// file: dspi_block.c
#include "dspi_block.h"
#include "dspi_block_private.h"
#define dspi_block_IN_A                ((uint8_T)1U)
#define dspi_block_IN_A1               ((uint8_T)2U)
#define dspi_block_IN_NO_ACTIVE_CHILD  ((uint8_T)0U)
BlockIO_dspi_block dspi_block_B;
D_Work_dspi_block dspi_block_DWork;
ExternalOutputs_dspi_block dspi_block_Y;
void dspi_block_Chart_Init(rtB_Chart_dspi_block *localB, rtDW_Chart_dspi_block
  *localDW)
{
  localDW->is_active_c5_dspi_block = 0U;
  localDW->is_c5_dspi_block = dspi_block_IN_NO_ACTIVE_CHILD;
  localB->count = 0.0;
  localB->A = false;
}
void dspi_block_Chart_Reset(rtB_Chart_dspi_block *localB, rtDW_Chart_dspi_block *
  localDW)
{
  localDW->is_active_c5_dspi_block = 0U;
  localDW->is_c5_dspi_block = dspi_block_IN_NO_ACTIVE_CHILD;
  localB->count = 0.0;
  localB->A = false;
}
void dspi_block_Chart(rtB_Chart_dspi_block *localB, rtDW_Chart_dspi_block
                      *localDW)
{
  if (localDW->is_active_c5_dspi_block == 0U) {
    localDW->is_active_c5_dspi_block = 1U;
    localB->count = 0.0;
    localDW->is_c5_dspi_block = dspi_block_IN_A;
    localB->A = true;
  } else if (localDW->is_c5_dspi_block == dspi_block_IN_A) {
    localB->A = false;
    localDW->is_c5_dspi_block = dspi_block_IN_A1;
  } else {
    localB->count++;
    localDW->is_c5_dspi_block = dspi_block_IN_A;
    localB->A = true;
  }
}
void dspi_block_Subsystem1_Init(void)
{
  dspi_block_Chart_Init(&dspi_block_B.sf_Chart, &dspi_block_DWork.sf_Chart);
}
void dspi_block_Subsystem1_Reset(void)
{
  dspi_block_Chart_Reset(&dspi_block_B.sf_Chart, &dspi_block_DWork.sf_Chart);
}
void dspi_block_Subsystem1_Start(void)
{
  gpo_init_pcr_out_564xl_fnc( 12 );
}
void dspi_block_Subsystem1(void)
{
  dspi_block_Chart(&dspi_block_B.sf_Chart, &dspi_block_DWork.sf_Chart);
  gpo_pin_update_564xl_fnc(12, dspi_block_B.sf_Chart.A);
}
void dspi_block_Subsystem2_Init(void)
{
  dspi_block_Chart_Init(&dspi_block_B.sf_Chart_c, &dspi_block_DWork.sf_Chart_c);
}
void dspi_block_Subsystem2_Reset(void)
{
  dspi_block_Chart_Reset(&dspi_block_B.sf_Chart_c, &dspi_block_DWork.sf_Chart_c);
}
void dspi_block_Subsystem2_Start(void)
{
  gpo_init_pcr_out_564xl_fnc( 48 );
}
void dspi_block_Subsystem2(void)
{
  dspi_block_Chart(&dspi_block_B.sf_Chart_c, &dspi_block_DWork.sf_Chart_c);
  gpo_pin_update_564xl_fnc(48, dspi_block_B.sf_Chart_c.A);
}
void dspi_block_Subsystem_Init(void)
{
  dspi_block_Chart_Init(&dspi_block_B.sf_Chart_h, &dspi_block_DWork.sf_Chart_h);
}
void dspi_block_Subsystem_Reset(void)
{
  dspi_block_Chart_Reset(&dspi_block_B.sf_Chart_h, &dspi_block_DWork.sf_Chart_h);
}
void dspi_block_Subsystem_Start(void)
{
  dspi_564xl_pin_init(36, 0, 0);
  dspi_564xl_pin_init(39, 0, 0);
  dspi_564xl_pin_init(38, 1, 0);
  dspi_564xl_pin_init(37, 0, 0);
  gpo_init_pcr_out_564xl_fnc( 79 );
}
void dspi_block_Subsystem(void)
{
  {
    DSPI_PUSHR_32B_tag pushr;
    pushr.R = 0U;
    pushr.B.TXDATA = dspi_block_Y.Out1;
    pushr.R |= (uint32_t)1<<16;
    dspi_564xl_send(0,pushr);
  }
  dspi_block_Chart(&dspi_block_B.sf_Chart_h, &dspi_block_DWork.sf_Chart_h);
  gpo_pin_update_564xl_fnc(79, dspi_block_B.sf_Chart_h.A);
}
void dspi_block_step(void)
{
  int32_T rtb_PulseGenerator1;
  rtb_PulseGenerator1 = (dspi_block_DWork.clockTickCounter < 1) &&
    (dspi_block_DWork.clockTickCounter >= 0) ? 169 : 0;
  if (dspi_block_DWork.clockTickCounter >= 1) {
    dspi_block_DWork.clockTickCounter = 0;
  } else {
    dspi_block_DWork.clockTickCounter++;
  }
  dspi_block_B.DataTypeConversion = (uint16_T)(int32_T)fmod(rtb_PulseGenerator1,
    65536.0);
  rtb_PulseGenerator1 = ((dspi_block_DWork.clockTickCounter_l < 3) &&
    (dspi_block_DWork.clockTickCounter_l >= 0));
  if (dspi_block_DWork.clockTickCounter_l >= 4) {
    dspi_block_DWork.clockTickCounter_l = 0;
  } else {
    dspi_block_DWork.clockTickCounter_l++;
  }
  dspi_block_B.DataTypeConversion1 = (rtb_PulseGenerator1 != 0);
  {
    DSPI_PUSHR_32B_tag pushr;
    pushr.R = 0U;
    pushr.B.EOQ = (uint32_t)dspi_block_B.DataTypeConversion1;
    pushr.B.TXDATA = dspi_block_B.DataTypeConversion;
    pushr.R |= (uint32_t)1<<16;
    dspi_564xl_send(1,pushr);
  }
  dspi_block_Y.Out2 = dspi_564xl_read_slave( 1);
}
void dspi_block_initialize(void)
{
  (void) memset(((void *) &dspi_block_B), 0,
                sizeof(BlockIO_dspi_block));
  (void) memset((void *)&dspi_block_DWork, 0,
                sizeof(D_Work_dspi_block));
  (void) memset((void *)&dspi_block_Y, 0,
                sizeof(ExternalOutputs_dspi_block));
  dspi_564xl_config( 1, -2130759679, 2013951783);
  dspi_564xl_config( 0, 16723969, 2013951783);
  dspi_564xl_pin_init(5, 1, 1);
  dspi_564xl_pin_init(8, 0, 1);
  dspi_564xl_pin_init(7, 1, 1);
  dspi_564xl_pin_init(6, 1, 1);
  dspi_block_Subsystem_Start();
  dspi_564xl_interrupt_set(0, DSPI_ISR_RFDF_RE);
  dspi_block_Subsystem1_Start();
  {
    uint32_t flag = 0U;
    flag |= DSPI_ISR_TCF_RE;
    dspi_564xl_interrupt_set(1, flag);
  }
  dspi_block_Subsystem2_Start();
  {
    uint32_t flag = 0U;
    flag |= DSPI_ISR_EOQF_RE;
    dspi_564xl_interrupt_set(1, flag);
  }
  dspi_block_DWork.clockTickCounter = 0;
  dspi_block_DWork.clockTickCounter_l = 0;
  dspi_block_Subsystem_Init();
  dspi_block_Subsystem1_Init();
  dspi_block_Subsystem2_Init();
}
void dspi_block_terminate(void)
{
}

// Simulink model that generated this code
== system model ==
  Out2 : Outport  <- 1: DSPIReceive#1
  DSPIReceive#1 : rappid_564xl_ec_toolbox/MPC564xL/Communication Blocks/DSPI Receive
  Out1 : Outport  <- 1: DSPIReceiveTrigger#1/2
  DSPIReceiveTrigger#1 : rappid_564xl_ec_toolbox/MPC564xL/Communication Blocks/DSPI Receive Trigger
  Subsystem1 : Subsystem  <- Trigger: DSPIISR#1
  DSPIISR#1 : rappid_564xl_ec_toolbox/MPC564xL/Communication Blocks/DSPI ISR
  Subsystem2 : Subsystem  <- Trigger: DSPIISR#2
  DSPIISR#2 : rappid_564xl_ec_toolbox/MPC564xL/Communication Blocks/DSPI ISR
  Subsystem : Subsystem  <- 1: DSPIReceiveTrigger#1/2, Trigger: DSPIReceiveTrigger#1
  DSPITransmit#1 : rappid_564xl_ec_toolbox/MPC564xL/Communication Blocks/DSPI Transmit  <- 1: DataTypeConversion, 2: DataTypeConversion1
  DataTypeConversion : DataTypeConversion  <- 1: DiscretePulseGenerator#1
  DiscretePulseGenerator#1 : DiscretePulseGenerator  Amplitude=169
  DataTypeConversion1 : DataTypeConversion  <- 1: PulseGenerator1
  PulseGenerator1 : DiscretePulseGenerator  Period=5  PulseWidth=3
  DSPIConfig#1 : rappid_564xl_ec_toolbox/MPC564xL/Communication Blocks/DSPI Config
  DSPIConfig#2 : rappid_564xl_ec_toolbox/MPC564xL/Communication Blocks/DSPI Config
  RAppID_564xL_Config#1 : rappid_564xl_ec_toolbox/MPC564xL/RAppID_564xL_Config
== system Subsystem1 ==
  TriggerPort#1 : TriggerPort  TriggerType=function-call
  DigitalOutput#1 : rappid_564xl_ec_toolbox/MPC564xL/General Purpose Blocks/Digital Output  <- 1: Chart/2
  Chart : Stateflow chart
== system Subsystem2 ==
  TriggerPort#2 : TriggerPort  TriggerType=function-call
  DigitalOutput#2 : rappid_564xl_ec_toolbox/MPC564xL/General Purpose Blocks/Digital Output  <- 1: Stateflowchart#1/2
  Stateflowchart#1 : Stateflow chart
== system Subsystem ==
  Inport#1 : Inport
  TriggerPort#3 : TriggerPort  TriggerType=function-call
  DigitalOutput#3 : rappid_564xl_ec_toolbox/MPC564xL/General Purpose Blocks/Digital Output  <- 1: Stateflowchart#2/2
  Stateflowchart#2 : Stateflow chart
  DSPITransmit#2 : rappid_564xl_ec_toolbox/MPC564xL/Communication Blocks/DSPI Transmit  <- 1: Inport#1
== stateflow chart Chart ==
  state A
  state A1
  (default) -> A : {count =0;}
  A -> A1
  A1 -> A : { count = count + 1;}
  data: count output double; A output boolean

== stateflow chart Chart ==
  state A
  state A1
  (default) -> A : {count =0;}
  A -> A1
  A1 -> A : { count = count + 1;}
  data: count output double; A output boolean

== stateflow chart Chart ==
  state A
  state A1
  (default) -> A : {count =0;}
  A -> A1
  A1 -> A : { count = count + 1;}
  data: count output double; A output boolean
